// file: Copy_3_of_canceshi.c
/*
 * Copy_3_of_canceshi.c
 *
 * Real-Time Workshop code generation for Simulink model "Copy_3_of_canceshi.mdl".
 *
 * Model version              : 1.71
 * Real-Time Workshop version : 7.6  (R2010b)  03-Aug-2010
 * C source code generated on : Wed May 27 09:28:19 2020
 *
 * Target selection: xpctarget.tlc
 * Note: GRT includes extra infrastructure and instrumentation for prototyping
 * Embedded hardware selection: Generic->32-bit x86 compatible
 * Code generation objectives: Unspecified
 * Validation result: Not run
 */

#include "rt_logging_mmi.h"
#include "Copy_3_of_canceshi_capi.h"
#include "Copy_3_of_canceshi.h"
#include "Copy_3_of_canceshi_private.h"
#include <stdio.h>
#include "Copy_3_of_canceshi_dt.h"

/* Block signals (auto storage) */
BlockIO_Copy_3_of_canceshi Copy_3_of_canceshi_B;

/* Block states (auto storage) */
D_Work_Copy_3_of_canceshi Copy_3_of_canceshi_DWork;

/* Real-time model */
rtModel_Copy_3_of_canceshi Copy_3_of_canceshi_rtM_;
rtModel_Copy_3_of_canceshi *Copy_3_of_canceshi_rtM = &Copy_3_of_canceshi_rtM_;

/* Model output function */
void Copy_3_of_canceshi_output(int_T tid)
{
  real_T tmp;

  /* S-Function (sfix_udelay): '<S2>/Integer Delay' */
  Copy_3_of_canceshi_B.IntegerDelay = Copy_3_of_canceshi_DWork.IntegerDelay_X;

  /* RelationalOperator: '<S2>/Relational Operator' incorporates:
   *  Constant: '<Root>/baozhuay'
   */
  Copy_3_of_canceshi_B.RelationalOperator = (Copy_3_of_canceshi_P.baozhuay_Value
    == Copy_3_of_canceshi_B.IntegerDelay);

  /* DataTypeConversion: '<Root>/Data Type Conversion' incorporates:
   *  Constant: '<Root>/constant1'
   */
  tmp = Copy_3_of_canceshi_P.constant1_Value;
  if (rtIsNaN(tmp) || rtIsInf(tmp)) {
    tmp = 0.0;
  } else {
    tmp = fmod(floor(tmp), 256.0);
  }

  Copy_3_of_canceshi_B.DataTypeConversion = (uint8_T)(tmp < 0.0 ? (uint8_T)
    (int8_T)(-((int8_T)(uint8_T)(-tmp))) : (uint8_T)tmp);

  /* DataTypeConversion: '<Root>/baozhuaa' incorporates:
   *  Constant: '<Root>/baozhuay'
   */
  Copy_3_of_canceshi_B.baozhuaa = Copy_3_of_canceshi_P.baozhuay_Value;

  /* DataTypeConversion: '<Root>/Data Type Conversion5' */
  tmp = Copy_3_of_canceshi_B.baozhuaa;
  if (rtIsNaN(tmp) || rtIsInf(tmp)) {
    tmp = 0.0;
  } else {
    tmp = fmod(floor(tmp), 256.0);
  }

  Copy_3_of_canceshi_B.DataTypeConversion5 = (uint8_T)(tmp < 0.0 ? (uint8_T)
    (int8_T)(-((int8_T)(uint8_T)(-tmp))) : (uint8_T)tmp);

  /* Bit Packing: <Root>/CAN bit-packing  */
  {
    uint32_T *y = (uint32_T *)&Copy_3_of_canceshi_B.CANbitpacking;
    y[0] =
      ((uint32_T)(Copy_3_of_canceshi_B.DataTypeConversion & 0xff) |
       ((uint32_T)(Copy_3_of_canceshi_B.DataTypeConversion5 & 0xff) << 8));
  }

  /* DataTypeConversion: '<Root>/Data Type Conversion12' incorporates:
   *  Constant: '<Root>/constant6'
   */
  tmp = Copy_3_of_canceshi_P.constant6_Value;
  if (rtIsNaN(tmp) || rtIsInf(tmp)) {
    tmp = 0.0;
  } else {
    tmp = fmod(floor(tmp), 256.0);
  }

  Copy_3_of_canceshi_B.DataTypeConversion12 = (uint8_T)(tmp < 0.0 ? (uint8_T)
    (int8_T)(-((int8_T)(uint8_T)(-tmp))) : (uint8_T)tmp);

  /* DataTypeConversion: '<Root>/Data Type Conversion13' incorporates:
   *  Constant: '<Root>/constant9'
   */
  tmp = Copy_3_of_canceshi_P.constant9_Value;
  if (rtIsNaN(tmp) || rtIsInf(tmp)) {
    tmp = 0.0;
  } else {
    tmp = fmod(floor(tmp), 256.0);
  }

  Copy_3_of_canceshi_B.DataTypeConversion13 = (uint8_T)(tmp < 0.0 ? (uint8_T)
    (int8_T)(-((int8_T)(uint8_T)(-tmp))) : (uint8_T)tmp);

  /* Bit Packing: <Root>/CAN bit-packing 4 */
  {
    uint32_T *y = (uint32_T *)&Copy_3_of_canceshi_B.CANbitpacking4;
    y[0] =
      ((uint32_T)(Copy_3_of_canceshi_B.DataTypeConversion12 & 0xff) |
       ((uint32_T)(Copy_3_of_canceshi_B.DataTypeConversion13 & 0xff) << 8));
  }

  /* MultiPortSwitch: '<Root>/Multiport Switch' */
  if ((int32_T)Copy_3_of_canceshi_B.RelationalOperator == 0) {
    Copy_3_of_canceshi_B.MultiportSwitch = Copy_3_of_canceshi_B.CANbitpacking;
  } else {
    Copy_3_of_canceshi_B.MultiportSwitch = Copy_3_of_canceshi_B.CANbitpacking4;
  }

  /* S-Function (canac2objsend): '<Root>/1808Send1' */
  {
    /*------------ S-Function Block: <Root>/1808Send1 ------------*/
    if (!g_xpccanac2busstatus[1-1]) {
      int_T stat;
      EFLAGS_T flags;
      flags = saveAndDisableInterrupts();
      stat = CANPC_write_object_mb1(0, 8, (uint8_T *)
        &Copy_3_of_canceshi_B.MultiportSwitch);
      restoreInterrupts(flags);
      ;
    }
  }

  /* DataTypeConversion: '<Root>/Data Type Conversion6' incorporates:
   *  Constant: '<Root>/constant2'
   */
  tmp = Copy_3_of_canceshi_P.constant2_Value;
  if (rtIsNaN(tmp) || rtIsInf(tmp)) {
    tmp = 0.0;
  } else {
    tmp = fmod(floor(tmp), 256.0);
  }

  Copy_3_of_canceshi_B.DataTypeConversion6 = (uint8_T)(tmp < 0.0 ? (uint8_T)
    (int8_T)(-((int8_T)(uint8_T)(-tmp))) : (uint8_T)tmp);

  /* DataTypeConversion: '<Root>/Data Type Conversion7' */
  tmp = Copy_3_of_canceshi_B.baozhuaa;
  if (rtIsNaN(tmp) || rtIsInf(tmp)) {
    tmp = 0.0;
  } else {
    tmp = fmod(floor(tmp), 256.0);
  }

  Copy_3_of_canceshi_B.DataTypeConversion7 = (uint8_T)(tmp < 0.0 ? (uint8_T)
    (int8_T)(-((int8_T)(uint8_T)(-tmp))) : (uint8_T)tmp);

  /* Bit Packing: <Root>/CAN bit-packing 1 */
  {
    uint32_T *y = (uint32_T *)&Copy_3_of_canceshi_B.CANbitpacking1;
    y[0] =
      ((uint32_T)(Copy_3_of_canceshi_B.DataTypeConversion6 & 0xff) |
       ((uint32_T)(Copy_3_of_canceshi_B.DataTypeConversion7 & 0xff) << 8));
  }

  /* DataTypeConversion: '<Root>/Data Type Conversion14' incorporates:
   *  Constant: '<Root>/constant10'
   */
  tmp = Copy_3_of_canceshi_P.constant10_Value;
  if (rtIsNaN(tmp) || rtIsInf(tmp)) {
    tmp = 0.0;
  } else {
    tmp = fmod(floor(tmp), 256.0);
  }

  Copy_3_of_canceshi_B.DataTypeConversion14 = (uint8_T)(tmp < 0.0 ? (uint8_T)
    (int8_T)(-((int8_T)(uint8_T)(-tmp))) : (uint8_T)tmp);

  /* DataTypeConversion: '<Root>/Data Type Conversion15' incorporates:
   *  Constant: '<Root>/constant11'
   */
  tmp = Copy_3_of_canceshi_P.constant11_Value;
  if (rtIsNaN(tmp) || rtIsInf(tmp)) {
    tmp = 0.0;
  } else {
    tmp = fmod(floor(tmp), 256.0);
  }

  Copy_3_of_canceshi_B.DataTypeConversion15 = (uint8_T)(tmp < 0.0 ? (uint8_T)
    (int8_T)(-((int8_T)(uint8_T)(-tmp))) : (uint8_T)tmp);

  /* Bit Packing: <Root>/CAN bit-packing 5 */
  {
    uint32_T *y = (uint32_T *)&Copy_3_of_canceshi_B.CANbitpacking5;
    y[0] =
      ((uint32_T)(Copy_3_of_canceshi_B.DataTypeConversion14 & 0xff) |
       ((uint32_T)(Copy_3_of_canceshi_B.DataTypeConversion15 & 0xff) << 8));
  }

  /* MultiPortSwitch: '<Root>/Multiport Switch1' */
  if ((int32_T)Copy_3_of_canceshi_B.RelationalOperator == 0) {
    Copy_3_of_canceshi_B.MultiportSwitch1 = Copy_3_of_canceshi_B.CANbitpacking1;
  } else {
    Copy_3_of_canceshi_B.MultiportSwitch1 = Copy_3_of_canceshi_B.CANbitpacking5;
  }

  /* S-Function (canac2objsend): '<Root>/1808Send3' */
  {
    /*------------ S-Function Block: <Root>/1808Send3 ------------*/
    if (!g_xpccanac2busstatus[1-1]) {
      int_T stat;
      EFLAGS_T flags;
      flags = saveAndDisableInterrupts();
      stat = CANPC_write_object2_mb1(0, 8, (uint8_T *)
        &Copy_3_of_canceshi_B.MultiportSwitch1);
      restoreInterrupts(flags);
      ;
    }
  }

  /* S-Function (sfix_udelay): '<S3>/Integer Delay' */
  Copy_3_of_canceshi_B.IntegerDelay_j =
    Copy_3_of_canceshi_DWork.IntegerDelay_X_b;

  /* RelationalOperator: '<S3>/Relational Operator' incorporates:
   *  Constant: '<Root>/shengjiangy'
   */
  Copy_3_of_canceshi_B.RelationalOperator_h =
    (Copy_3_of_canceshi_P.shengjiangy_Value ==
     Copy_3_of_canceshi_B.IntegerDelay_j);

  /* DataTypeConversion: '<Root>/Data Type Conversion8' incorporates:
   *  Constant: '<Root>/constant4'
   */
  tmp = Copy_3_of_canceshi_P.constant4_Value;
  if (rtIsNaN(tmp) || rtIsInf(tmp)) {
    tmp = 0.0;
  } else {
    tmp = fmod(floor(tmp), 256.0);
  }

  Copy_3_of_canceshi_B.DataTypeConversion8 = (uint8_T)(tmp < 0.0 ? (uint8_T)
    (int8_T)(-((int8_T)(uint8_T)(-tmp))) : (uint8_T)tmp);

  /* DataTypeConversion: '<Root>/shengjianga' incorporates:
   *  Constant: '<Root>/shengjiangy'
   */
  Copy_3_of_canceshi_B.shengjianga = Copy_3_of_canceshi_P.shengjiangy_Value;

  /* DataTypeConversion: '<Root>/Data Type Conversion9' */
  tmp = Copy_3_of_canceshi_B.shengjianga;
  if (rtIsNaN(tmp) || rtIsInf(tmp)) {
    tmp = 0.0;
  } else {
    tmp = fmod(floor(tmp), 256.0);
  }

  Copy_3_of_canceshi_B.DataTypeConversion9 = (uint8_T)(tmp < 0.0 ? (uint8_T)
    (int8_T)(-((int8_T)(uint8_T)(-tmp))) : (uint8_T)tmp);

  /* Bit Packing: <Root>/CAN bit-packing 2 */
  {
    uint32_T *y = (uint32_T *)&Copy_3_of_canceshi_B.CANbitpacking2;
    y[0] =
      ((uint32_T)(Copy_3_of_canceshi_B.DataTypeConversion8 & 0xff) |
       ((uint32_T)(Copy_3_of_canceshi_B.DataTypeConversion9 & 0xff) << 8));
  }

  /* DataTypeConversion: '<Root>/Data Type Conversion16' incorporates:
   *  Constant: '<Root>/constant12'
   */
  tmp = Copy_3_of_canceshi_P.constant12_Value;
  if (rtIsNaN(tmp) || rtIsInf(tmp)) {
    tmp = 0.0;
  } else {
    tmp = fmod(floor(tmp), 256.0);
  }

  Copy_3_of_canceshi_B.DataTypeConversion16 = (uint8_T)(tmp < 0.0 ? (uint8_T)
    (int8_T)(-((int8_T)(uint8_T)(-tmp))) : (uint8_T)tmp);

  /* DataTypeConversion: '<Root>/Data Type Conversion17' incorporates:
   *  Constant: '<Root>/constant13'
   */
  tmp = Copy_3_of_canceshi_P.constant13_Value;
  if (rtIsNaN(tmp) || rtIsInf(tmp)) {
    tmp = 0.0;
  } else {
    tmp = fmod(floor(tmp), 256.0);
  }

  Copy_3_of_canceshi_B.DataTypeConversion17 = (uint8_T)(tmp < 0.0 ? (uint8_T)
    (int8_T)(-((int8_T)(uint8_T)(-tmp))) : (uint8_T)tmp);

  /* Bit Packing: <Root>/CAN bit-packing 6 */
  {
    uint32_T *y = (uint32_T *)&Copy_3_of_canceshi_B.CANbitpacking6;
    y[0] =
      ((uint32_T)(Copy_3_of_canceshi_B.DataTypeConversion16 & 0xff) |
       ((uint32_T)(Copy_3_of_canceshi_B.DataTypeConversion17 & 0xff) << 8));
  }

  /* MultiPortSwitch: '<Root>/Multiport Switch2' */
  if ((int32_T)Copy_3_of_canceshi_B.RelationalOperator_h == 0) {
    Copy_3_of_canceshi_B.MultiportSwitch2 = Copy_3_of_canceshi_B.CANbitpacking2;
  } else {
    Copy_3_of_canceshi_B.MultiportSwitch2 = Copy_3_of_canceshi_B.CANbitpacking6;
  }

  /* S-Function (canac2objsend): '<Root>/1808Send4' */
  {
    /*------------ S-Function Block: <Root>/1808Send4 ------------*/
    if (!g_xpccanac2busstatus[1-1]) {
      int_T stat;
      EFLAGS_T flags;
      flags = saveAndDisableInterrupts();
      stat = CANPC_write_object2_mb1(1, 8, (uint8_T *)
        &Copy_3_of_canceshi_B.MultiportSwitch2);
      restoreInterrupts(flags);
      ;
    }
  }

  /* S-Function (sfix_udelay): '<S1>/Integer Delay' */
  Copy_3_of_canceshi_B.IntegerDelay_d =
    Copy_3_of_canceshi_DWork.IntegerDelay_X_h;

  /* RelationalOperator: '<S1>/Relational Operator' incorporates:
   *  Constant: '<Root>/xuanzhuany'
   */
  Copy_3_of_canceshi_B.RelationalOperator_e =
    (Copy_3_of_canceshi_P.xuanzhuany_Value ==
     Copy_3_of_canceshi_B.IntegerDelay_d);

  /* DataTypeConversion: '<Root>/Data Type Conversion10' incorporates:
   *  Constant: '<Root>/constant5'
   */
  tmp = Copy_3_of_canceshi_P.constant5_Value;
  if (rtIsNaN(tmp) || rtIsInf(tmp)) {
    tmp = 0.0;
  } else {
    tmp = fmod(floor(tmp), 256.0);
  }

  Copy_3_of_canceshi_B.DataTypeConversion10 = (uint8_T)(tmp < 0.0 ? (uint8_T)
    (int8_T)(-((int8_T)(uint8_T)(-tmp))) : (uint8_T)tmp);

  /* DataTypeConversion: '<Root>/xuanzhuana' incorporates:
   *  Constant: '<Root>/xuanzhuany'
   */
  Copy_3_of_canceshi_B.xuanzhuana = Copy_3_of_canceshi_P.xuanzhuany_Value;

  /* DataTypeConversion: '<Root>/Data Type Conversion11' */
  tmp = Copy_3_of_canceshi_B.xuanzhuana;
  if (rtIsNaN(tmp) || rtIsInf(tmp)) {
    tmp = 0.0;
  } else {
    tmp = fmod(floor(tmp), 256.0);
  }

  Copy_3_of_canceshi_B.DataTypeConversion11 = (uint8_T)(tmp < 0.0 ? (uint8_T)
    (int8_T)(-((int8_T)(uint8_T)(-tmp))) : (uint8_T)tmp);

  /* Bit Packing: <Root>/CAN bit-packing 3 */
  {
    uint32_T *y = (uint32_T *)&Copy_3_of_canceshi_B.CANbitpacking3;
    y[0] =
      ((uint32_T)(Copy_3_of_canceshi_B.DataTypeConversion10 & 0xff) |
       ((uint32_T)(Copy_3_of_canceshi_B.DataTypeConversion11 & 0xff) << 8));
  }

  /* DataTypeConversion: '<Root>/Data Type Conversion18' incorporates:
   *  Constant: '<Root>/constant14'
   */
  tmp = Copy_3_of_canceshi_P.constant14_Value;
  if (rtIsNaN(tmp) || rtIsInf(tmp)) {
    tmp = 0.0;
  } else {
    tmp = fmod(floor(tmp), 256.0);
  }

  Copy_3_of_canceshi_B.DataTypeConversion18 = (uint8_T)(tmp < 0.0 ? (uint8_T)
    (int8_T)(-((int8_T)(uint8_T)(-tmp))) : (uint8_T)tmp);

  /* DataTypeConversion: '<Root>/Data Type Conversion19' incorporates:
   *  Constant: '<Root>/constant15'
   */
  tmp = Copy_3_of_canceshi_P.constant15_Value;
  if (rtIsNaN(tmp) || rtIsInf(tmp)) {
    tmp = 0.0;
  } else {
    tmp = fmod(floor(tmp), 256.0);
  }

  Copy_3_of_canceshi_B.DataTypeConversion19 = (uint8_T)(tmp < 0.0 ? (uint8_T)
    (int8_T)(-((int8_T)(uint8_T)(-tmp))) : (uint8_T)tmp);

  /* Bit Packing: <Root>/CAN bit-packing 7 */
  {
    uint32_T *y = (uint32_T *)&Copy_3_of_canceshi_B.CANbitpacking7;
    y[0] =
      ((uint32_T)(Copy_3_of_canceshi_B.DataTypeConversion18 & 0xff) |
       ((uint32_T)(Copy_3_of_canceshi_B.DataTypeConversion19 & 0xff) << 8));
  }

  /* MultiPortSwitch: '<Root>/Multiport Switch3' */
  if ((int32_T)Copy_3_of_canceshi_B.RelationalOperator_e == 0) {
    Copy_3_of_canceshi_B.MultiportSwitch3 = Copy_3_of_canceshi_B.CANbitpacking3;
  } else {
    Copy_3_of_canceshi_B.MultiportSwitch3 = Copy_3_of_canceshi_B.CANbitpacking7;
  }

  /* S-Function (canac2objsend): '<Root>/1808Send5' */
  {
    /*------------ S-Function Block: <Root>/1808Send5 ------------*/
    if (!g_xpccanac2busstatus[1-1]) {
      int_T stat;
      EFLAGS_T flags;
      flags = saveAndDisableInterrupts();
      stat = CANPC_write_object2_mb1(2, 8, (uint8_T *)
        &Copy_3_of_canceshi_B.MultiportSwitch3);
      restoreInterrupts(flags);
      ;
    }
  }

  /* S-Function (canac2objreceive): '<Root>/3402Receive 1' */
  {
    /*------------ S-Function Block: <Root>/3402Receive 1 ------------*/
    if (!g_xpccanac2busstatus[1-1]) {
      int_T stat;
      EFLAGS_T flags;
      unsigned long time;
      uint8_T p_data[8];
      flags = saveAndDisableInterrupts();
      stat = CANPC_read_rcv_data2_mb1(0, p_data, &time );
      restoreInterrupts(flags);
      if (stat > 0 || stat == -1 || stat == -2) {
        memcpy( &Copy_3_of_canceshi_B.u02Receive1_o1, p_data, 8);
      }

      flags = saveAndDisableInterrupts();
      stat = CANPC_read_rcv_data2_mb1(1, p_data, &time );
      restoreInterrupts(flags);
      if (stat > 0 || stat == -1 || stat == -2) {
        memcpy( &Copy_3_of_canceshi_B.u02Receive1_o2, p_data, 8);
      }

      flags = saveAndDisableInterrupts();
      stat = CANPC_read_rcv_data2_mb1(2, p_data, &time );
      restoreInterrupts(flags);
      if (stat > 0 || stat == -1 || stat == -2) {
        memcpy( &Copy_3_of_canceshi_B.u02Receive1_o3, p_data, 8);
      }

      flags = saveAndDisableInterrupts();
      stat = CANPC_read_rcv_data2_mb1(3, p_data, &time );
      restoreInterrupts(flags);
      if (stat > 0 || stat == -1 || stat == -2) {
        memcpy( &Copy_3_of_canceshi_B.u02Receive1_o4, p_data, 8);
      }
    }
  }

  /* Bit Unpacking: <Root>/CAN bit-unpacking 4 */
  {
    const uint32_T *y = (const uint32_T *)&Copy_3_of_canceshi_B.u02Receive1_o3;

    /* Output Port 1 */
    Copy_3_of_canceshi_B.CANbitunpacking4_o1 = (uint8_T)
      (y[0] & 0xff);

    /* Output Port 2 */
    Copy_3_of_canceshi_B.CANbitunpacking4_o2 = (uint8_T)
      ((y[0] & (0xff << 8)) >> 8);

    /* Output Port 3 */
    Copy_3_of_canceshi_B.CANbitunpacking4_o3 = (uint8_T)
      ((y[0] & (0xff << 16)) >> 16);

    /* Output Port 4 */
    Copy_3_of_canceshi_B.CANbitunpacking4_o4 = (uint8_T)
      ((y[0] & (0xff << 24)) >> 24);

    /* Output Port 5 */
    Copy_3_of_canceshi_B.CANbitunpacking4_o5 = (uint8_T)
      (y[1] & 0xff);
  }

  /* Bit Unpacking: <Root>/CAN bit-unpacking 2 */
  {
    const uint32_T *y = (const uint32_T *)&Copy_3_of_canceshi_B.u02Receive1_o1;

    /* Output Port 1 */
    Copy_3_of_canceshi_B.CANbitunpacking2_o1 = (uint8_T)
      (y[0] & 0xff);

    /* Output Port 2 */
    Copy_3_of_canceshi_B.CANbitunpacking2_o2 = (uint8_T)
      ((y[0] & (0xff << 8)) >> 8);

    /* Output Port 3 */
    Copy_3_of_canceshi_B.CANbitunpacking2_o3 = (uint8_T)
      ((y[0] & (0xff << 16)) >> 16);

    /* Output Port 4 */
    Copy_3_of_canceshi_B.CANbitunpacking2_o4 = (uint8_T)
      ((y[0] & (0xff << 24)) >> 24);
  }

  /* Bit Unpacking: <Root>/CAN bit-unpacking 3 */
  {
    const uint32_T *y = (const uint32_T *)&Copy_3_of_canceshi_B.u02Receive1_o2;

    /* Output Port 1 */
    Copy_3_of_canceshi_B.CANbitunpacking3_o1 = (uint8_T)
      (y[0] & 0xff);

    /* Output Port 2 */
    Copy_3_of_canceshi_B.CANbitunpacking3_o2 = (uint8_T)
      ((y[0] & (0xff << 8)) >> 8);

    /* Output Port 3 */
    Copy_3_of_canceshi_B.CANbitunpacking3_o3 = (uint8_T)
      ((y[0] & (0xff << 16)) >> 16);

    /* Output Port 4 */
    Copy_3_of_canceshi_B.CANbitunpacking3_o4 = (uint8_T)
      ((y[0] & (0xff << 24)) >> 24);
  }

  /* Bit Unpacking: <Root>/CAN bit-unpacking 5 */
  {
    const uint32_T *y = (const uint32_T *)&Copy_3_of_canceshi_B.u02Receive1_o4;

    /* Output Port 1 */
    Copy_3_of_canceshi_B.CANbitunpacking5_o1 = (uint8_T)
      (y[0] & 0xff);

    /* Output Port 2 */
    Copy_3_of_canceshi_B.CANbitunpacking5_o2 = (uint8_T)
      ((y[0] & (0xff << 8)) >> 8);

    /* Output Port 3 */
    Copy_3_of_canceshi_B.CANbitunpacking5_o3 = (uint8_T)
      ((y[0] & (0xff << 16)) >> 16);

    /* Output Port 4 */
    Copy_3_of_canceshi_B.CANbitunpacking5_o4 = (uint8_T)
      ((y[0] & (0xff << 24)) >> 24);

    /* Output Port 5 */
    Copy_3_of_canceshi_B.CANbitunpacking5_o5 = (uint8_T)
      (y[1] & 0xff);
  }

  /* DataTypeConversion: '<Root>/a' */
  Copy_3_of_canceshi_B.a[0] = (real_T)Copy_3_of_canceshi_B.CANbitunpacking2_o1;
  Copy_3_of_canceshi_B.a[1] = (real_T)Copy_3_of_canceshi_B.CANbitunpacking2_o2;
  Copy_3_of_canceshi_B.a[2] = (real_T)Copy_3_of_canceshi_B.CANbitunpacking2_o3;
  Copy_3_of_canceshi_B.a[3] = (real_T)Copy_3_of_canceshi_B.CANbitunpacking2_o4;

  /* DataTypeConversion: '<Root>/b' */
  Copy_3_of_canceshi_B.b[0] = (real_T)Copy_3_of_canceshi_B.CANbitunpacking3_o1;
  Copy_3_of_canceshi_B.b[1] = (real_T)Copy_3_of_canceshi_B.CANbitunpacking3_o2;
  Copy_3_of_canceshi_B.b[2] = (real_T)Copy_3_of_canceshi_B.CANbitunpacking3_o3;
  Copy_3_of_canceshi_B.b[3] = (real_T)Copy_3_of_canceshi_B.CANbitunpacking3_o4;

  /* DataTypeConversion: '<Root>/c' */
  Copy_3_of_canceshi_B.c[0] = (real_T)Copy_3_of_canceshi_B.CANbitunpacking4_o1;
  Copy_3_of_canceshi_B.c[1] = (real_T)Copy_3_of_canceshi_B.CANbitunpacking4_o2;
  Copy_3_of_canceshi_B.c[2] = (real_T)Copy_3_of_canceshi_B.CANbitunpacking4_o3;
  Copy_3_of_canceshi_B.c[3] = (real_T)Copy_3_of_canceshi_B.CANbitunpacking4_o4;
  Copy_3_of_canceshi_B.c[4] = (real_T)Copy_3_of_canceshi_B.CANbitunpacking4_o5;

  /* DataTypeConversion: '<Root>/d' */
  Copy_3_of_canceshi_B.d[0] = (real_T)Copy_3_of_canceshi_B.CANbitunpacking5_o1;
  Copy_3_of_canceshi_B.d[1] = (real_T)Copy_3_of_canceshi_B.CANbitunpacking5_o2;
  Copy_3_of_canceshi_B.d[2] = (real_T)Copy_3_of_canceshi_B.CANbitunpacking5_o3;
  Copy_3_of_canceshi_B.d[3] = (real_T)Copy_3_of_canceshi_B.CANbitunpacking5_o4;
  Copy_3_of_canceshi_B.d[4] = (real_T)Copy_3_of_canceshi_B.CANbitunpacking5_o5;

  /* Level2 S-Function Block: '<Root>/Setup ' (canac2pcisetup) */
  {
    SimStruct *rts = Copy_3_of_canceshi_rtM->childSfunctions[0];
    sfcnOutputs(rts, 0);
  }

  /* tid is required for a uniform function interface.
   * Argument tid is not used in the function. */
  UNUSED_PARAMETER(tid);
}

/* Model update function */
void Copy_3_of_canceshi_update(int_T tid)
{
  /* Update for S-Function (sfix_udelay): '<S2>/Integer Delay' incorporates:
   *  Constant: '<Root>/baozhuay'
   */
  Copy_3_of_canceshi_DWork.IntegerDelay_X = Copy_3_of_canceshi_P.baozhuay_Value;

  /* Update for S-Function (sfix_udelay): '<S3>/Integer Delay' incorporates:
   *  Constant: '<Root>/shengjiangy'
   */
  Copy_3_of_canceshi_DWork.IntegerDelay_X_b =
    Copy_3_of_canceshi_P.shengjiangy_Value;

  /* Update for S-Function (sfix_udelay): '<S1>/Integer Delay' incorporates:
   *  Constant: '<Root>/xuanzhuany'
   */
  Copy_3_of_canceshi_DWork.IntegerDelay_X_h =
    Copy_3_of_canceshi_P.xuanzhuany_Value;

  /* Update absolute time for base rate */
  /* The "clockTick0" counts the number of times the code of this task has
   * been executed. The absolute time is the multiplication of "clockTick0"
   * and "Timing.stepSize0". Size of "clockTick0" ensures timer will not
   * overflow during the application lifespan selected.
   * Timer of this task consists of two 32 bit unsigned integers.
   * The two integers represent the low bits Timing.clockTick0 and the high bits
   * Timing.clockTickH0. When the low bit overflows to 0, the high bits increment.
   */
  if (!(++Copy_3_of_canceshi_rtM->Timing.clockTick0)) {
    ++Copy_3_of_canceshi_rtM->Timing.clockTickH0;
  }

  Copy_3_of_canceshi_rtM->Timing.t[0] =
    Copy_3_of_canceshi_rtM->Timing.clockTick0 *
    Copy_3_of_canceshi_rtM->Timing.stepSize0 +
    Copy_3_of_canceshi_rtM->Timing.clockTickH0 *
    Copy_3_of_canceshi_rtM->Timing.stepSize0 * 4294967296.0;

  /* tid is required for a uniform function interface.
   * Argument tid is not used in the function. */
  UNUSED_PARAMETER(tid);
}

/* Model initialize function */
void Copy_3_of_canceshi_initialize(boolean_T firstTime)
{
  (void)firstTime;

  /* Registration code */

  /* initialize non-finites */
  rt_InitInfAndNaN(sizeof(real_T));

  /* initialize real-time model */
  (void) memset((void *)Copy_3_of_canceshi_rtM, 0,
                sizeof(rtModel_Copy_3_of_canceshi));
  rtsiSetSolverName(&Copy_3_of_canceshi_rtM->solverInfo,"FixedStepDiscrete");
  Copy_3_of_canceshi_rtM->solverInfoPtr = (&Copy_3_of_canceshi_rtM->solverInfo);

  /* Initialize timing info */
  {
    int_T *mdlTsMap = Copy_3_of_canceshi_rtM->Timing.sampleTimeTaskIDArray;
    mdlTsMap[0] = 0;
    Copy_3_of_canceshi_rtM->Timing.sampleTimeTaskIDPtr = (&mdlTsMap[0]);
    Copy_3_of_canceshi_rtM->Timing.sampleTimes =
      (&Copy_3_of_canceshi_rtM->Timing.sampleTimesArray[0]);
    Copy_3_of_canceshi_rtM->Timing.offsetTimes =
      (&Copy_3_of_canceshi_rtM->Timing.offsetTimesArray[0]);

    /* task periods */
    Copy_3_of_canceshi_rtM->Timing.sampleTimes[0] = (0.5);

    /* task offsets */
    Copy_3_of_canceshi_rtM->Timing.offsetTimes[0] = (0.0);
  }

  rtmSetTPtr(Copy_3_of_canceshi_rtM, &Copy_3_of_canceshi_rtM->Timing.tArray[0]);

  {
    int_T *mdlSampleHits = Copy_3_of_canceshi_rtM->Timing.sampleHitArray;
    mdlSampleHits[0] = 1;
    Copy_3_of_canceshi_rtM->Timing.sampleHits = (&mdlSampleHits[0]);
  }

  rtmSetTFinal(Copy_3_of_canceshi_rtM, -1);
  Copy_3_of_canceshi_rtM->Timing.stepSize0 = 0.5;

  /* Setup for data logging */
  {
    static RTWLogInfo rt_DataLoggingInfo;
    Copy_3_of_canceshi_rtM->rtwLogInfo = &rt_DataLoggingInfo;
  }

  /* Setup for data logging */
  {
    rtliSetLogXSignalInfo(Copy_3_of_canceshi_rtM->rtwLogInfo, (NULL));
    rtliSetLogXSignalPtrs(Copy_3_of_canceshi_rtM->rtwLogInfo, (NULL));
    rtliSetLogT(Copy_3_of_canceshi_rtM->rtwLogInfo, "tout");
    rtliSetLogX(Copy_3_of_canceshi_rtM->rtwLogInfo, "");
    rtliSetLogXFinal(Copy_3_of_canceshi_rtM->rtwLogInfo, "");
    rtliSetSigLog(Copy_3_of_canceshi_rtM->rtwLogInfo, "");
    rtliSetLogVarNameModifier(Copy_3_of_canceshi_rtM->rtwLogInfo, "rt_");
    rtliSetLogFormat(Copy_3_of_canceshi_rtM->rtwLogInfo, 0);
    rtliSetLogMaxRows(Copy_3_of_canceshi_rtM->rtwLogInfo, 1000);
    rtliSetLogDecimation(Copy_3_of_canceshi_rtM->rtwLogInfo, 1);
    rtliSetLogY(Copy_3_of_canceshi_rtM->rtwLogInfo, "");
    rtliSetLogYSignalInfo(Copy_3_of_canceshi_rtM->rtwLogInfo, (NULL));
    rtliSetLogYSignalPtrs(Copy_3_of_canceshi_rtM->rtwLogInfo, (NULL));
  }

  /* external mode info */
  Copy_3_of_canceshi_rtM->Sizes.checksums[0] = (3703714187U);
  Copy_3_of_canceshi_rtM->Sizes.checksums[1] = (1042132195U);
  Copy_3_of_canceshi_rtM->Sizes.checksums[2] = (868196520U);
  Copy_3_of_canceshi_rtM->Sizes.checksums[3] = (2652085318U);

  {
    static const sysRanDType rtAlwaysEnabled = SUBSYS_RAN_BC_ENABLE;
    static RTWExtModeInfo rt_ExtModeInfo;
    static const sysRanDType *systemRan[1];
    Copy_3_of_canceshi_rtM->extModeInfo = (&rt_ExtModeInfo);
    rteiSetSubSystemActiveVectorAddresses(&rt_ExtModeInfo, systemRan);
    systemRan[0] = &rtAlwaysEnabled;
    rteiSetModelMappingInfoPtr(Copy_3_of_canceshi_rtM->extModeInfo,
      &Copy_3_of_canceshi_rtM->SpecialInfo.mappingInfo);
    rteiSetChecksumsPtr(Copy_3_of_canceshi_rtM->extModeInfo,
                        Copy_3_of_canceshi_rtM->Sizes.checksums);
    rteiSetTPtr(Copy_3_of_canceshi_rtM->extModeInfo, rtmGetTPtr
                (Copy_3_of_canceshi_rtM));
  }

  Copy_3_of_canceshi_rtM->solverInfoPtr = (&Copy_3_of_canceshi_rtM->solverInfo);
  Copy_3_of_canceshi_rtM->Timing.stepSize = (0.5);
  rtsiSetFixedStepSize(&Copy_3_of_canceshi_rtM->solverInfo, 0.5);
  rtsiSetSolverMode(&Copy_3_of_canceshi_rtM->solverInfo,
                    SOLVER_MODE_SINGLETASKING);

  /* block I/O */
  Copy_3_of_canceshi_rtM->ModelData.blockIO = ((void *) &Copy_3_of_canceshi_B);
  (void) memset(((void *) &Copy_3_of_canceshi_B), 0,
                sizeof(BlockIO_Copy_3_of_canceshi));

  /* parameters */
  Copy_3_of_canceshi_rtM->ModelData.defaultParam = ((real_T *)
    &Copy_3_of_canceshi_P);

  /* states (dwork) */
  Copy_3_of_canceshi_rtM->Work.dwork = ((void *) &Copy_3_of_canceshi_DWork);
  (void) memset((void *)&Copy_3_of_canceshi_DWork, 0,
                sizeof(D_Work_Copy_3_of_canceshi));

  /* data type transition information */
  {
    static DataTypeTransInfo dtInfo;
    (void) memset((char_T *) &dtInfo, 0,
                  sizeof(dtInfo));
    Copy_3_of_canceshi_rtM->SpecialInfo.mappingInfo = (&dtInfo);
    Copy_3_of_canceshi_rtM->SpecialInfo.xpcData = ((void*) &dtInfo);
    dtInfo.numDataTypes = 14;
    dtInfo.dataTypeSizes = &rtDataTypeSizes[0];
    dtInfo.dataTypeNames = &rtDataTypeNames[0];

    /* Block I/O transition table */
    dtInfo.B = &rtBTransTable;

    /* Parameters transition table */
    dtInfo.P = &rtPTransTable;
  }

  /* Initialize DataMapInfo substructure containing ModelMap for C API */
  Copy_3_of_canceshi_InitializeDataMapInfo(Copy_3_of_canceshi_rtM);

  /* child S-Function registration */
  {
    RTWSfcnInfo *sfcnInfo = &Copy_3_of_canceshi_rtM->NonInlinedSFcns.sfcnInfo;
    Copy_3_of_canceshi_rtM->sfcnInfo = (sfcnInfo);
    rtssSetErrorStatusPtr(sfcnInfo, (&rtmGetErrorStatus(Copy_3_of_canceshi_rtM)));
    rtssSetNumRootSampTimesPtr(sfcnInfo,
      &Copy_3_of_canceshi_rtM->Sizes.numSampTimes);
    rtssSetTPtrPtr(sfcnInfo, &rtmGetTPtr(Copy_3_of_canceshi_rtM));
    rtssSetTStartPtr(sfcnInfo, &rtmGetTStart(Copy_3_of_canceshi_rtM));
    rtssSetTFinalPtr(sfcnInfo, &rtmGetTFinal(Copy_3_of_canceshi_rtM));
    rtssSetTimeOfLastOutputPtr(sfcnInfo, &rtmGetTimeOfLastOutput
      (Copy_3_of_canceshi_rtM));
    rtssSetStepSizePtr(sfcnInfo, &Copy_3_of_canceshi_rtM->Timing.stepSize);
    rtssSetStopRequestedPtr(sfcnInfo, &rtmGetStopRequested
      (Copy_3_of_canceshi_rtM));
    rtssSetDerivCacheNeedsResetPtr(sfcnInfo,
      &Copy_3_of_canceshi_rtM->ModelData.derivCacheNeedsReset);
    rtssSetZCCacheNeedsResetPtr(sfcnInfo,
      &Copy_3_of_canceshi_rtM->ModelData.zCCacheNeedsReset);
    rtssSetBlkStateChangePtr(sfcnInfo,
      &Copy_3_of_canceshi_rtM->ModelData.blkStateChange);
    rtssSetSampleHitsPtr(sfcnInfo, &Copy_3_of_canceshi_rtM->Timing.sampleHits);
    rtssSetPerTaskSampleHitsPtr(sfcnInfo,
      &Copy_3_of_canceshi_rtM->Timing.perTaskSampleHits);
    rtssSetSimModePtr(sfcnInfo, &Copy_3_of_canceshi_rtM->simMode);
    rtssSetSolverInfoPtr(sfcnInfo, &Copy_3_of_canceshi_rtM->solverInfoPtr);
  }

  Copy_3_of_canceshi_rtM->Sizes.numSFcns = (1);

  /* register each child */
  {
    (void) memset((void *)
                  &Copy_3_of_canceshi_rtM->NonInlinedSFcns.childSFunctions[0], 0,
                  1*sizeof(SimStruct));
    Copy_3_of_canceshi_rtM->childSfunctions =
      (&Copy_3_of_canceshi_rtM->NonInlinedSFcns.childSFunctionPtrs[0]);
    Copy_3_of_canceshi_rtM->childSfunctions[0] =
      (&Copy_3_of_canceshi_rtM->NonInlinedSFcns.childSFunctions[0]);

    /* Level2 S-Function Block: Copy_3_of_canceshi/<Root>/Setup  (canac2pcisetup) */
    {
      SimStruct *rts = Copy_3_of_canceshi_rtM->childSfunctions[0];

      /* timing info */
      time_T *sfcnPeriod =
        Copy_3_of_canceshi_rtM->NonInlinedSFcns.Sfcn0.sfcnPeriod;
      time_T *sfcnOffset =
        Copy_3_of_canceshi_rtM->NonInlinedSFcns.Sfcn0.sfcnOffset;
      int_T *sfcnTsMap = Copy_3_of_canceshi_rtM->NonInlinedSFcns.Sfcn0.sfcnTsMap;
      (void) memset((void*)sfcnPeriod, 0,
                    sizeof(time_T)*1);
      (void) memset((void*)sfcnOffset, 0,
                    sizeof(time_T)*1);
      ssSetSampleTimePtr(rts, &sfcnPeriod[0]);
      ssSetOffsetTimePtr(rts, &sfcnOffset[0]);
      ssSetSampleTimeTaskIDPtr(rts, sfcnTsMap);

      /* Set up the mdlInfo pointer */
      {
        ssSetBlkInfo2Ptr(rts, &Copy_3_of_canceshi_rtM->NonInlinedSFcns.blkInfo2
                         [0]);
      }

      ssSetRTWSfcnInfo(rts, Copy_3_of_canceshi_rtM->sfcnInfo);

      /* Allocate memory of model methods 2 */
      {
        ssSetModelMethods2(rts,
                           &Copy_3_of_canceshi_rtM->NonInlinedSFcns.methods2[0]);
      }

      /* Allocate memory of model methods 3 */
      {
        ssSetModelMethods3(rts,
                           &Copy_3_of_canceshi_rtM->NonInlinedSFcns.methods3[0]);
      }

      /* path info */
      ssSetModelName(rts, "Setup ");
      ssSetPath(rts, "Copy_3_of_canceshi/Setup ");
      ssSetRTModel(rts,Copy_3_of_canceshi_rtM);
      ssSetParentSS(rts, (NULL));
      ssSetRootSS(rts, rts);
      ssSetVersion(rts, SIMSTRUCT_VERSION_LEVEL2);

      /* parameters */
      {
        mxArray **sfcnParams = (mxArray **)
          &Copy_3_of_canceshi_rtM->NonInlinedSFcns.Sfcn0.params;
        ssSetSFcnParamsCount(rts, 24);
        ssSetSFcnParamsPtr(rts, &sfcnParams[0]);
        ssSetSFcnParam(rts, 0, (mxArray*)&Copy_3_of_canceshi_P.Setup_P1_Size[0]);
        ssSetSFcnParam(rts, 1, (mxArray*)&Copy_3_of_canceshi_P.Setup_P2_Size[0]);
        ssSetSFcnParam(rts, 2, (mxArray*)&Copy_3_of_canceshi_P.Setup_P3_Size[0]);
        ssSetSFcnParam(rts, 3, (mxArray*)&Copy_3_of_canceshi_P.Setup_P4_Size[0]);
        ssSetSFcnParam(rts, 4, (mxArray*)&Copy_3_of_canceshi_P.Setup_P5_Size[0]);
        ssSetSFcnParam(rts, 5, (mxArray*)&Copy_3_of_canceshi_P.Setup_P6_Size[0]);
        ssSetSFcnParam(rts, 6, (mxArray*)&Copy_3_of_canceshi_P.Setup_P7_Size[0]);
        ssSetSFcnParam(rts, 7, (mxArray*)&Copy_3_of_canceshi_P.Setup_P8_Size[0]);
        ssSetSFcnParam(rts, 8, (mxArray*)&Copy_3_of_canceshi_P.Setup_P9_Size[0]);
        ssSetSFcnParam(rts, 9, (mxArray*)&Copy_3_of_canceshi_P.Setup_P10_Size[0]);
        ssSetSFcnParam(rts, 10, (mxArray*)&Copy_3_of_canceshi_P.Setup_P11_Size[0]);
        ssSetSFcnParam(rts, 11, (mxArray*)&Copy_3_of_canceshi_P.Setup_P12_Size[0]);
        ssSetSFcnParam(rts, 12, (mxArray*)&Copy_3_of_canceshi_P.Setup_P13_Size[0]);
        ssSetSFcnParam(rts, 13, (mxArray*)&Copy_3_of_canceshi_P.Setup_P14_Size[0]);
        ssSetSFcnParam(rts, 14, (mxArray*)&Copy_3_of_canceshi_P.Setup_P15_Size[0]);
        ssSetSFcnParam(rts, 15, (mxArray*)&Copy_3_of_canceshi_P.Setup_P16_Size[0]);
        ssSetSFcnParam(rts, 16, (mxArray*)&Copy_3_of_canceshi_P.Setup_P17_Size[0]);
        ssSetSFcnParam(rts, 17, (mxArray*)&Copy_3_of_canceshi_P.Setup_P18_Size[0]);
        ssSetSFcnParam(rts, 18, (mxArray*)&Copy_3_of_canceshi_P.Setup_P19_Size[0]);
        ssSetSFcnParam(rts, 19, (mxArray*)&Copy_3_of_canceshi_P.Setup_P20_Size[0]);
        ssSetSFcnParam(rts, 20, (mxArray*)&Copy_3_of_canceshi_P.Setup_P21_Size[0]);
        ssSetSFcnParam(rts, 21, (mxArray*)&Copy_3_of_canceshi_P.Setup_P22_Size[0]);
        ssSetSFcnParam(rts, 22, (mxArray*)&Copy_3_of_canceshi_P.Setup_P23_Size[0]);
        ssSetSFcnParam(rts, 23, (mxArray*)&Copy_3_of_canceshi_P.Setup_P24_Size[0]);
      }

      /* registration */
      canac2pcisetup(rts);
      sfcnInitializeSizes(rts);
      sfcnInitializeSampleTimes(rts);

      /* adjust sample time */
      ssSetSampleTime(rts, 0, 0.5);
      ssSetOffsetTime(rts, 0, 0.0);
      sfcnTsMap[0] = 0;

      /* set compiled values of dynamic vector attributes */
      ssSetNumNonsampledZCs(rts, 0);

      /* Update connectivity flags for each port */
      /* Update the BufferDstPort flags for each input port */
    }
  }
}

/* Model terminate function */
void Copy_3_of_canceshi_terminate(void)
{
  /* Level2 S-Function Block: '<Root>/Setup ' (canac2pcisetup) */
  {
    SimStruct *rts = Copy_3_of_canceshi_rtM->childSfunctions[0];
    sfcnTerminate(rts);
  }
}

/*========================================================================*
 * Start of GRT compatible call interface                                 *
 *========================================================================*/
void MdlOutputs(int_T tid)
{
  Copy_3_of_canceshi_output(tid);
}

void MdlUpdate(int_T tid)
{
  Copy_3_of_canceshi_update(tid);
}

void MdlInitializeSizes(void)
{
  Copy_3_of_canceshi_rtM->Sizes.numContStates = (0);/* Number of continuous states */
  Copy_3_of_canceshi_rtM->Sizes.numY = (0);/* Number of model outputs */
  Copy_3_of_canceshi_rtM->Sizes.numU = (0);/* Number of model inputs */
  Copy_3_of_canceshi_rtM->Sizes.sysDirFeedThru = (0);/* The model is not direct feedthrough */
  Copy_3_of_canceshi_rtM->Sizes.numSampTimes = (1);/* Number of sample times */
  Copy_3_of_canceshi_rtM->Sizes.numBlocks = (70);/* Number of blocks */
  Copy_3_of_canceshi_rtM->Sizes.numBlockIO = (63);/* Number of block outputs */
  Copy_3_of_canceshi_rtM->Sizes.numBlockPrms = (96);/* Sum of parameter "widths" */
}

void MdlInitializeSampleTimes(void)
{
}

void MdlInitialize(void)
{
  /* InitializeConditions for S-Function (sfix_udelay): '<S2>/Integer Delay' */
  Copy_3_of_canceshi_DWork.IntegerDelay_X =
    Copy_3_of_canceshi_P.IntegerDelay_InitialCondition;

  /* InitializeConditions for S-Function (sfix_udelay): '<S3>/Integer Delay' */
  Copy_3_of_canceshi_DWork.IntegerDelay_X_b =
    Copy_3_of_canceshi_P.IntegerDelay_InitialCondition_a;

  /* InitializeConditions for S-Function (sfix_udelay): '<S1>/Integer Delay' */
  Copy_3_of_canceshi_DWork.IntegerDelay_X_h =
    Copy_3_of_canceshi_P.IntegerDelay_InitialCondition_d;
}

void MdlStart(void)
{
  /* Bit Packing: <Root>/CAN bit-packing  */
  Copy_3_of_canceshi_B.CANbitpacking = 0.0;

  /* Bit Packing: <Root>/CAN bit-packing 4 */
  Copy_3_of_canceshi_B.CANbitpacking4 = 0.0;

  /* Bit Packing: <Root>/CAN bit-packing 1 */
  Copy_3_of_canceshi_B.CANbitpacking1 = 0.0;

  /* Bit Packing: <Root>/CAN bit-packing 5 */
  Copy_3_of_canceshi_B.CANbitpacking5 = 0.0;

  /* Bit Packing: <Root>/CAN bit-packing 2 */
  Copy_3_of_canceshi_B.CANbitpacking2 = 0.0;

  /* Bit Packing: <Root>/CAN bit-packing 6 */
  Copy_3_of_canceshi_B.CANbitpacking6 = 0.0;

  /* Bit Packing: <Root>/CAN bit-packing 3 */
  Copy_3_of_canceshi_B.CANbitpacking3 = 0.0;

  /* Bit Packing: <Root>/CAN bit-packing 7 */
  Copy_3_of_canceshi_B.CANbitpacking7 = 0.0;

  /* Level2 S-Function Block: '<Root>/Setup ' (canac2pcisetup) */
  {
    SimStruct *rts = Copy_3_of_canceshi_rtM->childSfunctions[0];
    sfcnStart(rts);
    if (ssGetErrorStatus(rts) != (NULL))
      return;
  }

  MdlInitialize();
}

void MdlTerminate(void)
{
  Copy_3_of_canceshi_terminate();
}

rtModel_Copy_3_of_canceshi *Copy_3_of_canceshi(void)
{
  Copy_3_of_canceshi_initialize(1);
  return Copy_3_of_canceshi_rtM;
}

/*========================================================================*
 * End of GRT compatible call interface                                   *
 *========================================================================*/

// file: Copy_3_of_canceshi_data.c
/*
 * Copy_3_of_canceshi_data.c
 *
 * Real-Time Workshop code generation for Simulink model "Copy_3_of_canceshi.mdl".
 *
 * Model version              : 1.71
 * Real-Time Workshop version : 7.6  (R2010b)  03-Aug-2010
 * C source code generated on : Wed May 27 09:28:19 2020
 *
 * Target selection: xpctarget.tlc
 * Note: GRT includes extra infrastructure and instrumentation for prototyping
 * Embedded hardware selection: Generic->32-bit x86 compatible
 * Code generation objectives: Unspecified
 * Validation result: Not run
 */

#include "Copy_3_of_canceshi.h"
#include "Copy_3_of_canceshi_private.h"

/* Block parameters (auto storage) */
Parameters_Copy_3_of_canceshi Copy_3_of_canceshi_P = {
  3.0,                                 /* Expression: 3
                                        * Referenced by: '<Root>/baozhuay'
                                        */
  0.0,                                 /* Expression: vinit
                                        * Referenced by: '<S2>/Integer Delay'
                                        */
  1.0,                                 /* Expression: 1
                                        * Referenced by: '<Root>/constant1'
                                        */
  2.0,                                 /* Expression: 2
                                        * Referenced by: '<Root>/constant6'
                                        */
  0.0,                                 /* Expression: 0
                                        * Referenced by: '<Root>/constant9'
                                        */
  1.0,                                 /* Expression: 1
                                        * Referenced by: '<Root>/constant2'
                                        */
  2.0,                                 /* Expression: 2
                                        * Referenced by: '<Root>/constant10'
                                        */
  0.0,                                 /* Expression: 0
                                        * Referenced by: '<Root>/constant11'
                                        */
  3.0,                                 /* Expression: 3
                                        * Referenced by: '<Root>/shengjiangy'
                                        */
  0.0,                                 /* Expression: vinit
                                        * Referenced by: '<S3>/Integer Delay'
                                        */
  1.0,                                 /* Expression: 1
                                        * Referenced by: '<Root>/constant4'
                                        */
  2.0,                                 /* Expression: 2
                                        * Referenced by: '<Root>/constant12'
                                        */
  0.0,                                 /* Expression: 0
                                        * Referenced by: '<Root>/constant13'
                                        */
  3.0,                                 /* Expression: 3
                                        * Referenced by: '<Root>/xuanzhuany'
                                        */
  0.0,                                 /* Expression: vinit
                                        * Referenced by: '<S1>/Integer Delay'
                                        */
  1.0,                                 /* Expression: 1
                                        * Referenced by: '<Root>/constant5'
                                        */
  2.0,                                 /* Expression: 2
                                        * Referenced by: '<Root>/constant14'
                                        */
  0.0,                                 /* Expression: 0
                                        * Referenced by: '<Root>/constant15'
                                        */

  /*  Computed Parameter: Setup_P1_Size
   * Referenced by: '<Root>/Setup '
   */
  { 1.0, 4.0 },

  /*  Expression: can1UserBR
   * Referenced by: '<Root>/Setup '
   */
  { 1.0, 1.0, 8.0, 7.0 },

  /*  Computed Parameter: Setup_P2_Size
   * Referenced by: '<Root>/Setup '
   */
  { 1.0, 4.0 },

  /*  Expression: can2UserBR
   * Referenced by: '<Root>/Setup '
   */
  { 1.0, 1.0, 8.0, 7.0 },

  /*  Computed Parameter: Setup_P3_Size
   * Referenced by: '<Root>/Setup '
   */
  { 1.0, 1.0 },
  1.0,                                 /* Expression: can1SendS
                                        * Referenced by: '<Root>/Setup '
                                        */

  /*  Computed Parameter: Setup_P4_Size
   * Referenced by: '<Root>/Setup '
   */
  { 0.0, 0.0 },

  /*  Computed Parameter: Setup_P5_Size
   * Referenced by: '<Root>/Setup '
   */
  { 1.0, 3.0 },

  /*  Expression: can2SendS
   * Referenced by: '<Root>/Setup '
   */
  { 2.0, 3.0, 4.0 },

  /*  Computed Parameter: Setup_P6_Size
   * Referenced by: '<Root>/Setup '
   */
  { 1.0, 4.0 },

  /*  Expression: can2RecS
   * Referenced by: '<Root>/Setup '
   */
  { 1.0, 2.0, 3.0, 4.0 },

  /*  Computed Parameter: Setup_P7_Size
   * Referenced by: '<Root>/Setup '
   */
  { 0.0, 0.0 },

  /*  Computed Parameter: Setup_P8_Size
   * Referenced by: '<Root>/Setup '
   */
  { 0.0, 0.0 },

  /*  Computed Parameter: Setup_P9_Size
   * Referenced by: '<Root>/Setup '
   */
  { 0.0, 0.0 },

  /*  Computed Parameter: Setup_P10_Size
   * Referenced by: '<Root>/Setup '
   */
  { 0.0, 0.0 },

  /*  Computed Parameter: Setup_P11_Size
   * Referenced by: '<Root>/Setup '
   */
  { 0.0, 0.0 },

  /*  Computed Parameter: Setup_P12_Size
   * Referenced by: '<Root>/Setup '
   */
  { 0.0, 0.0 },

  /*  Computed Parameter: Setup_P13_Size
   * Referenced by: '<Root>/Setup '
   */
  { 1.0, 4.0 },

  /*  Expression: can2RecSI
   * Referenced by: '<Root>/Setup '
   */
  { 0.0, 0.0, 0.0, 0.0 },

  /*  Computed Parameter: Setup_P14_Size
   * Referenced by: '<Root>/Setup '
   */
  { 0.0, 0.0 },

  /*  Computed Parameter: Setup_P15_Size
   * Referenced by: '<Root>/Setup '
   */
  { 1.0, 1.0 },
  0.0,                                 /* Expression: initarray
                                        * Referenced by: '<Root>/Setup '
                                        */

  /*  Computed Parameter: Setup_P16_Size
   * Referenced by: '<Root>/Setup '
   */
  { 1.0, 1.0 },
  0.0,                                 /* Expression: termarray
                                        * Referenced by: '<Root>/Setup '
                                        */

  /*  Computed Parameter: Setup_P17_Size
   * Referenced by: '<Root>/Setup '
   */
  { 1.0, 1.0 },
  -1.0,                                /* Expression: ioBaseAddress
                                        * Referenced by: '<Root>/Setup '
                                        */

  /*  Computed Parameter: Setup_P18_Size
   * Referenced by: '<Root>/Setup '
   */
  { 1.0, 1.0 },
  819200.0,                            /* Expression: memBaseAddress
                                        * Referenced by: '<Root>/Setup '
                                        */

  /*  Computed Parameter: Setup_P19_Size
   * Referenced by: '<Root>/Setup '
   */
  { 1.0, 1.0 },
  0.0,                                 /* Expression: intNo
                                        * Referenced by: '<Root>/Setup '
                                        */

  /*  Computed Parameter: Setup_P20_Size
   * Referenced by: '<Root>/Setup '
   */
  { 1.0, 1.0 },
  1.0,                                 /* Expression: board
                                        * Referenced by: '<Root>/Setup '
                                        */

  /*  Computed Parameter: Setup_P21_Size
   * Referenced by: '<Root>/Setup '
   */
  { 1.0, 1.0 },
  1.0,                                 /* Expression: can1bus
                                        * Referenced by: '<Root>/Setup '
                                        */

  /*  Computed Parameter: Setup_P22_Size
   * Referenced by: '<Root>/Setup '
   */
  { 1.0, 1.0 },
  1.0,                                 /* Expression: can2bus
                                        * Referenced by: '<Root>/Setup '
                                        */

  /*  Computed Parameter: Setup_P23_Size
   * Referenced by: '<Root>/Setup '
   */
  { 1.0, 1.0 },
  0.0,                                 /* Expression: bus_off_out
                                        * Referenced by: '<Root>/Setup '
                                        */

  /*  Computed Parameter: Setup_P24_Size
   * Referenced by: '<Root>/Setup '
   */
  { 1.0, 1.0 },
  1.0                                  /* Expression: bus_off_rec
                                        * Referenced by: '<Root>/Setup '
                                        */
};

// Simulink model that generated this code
simulink model "Copy_3_of_canceshi"  (Simulink 7.6)
settings: Solver=ode4  StartTime=0.0  StopTime=inf  FixedStep=0.5  RelTol=1e-3
undefined symbols (not defined in the file or in its folder): bit, Standard
libraries: xpclib x18, simulink x3

== system Copy_3_of_canceshi ==
  1808Send1 : xpclib/CAN/Softing/CAN-AC2-PCI SJA 1000/Send   board=1  canPort=CAN 1  range=Standard (11-bit)  ids=1  sizes=[8]  output=off  ts=-1  ididx=[0]
  1808Send3 : xpclib/CAN/Softing/CAN-AC2-PCI SJA 1000/Send   board=1  canPort=CAN 2  range=Standard (11-bit)  ids=2  sizes=[8]  output=off  ts=-1  ididx=[1]
  1808Send4 : xpclib/CAN/Softing/CAN-AC2-PCI SJA 1000/Send   board=1  canPort=CAN 2  range=Standard (11-bit)  ids=3  sizes=[8]  output=off  ts=-1  ididx=[2]
  1808Send5 : xpclib/CAN/Softing/CAN-AC2-PCI SJA 1000/Send   board=1  canPort=CAN 2  range=Standard (11-bit)  ids=4  sizes=[8]  output=off  ts=-1  ididx=[3]
  3402Receive 1 : xpclib/CAN/Softing/CAN-AC2-PCI SJA 1000/Receive   board=1  canPort=CAN 2  range=Standard (11-bit)  ids=[1 2 3 4]  lengths=8  output=Data  inten=off  ts=-1  ididx=[0,1,2,3]
  CAN bit-packing {,1..7} (8 alike) : xpclib/CAN/Utilities/CAN bit-packing   bitpatterns={ [0:7] [8:15] }
  CAN bit-unpacking 2 : xpclib/CAN/Utilities/CAN bit-unpacking   bitpatterns={ [0:7],[8:15],[16:23],[24:31]}  dtypes={ 'uint8','uint8','uint8','uint8' }
  CAN bit-unpacking 3 : xpclib/CAN/Utilities/CAN bit-unpacking   bitpatterns={ [0:7],[8:15],[16:23],[24:31]}  dtypes={ 'uint8','uint8','uint8','uint8' }
  CAN bit-unpacking 4 : xpclib/CAN/Utilities/CAN bit-unpacking   bitpatterns={ [0:7],[8:15],[16:23],[24:31],[32:39]}  dtypes={ 'uint8','uint8','uint8','uint8','uint8' }
  CAN bit-unpacking 5 : xpclib/CAN/Utilities/CAN bit-unpacking   bitpatterns={ [0:7],[8:15],[16:23],[24:31],[32:39]}  dtypes={ 'uint8','uint8','uint8','uint8','uint8' }
  Data Type Conversion{,5..19} (16 alike) : DataTypeConversion  OutDataTypeStr=uint8
  Multiport Switch{,1..3} (4 alike) : MultiPortSwitch  DataPortOrder=Zero-based contiguous  Inputs=2  zeroidx=on
  Mux3 : Mux
  Mux4 : Mux
  Mux5 : Mux  Inputs=5
  Mux6 : Mux  Inputs=5
  "Setup " : xpclib/CAN/Softing/CAN-AC2-PCI SJA 1000/Setup   board=1  can1bus=Highspeed (ISO 11898)  can1Baudrate=500 kBaud  can1UserBR=[1,1,4,3]  can2bus=Highspeed (ISO 11898)  can2Baudrate=500 kBaud  can2UserBR=[1,1,4,3]  init=[]  term=[]  bus_off_out=off  bus_off_rec=Off  ioBaseAddress=-1
  Subsystem1 : Subsystem
  Subsystem2 : Subsystem
  Subsystem3 : Subsystem
  Terminator{1..4} (4 alike) : Terminator
  a : DataTypeConversion  OutDataTypeStr=double
  b : DataTypeConversion  OutDataTypeStr=double
  baozhuaa : DataTypeConversion
  baozhuay : Constant  Value=3
  c : DataTypeConversion  OutDataTypeStr=double
  chuanganqi{1..4} (4 alike) : Display
  constant{1..2,4..5} (4 alike) : Constant
  constant{6,10,12,14} (4 alike) : Constant  Value=2
  constant{9,11,13,15} (4 alike) : Constant  Value=0
  d : DataTypeConversion  OutDataTypeStr=double
  shengjianga : DataTypeConversion
  shengjiangy : Constant  Value=3
  xuanzhuana : DataTypeConversion
  xuanzhuany : Constant  Value=3
  wires:
  3402Receive 1/1 -> CAN bit-unpacking 2/1
  3402Receive 1/2 -> CAN bit-unpacking 3/1
  3402Receive 1/3 -> CAN bit-unpacking 4/1
  3402Receive 1/4 -> CAN bit-unpacking 5/1
  CAN bit-unpacking 2/1 -> Mux3/1
  CAN bit-unpacking 2/2 -> Mux3/2
  CAN bit-unpacking 2/3 -> Mux3/3
  CAN bit-unpacking 2/4 -> Mux3/4
  CAN bit-unpacking 3/1 -> Mux4/1
  CAN bit-unpacking 3/2 -> Mux4/2
  CAN bit-unpacking 3/3 -> Mux4/3
  CAN bit-unpacking 3/4 -> Mux4/4
  CAN bit-unpacking 4/1 -> Mux5/1
  CAN bit-unpacking 4/2 -> Mux5/2
  CAN bit-unpacking 4/3 -> Mux5/3
  CAN bit-unpacking 4/4 -> Mux5/4
  CAN bit-unpacking 4/5 -> Mux5/5
  CAN bit-unpacking 5/1 -> Mux6/1
  CAN bit-unpacking 5/2 -> Mux6/2
  CAN bit-unpacking 5/3 -> Mux6/3
  CAN bit-unpacking 5/4 -> Mux6/4
  CAN bit-unpacking 5/5 -> Mux6/5
  Mux3/1 -> chuanganqi2/1, a/1
  Mux4/1 -> b/1, chuanganqi3/1
  Mux5/1 -> c/1, chuanganqi1/1
  Mux6/1 -> d/1, chuanganqi4/1
  b/1 -> Terminator1/1
  c/1 -> Terminator2/1
  d/1 -> Terminator3/1
  a/1 -> Terminator4/1
  constant1/1 -> Data Type Conversion/1
  Data Type Conversion/1 -> "CAN bit-packing "/1
  Data Type Conversion5/1 -> "CAN bit-packing "/2
  constant2/1 -> Data Type Conversion6/1
  Data Type Conversion6/1 -> CAN bit-packing 1/1
  Data Type Conversion7/1 -> CAN bit-packing 1/2
  constant4/1 -> Data Type Conversion8/1
  Data Type Conversion8/1 -> CAN bit-packing 2/1
  Data Type Conversion9/1 -> CAN bit-packing 2/2
  constant5/1 -> Data Type Conversion10/1
  Data Type Conversion10/1 -> CAN bit-packing 3/1
  Data Type Conversion11/1 -> CAN bit-packing 3/2
  constant6/1 -> Data Type Conversion12/1
  Data Type Conversion12/1 -> CAN bit-packing 4/1
  Data Type Conversion13/1 -> CAN bit-packing 4/2
  constant9/1 -> Data Type Conversion13/1
  constant10/1 -> Data Type Conversion14/1
  Data Type Conversion14/1 -> CAN bit-packing 5/1
  Data Type Conversion15/1 -> CAN bit-packing 5/2
  constant11/1 -> Data Type Conversion15/1
  constant12/1 -> Data Type Conversion16/1
  Data Type Conversion16/1 -> CAN bit-packing 6/1
  Data Type Conversion17/1 -> CAN bit-packing 6/2
  constant13/1 -> Data Type Conversion17/1
  constant14/1 -> Data Type Conversion18/1
  Data Type Conversion18/1 -> CAN bit-packing 7/1
  Data Type Conversion19/1 -> CAN bit-packing 7/2
  constant15/1 -> Data Type Conversion19/1
  Multiport Switch1/1 -> 1808Send3/1
  baozhuay/1 -> baozhuaa/1, Subsystem2/1(In1)
  shengjiangy/1 -> shengjianga/1, Subsystem3/1(In1)
  shengjianga/1 -> Data Type Conversion9/1
  xuanzhuany/1 -> xuanzhuana/1, Subsystem1/1(In1)
  xuanzhuana/1 -> Data Type Conversion11/1
  Multiport Switch3/1 -> 1808Send5/1
  Multiport Switch/1 -> 1808Send1/1
  Multiport Switch2/1 -> 1808Send4/1
  "CAN bit-packing "/1 -> Multiport Switch/2
  CAN bit-packing 4/1 -> Multiport Switch/3
  CAN bit-packing 1/1 -> Multiport Switch1/2
  CAN bit-packing 5/1 -> Multiport Switch1/3
  CAN bit-packing 2/1 -> Multiport Switch2/2
  CAN bit-packing 6/1 -> Multiport Switch2/3
  CAN bit-packing 3/1 -> Multiport Switch3/2
  CAN bit-packing 7/1 -> Multiport Switch3/3
  baozhuaa/1 -> Data Type Conversion5/1, Data Type Conversion7/1
  Subsystem2/1(Out1) -> Multiport Switch/1, Multiport Switch1/1
  Subsystem3/1(Out1) -> Multiport Switch2/1
  Subsystem1/1(Out1) -> Multiport Switch3/1

== system Copy_3_of_canceshi/Subsystem1 ==
  In1 : Inport
  Integer Delay : simulink/Discrete/Integer Delay  NumDelays=1  vinit=0.0  samptime=-1
  Relational Operator : RelationalOperator  Operator===  OutDataTypeStr=boolean
  Out1 : Outport
  wires:
  Integer Delay/1 -> Relational Operator/2
  In1/1 -> Integer Delay/1, Relational Operator/1
  Relational Operator/1 -> Out1/1

== system Copy_3_of_canceshi/Subsystem2 ==
  In1 : Inport
  Integer Delay : simulink/Discrete/Integer Delay  NumDelays=1  vinit=0.0  samptime=-1
  Relational Operator : RelationalOperator  Operator===  OutDataTypeStr=boolean
  Out1 : Outport
  wires:
  Integer Delay/1 -> Relational Operator/2
  In1/1 -> Integer Delay/1, Relational Operator/1
  Relational Operator/1 -> Out1/1

== system Copy_3_of_canceshi/Subsystem3 ==
  In1 : Inport
  Integer Delay : simulink/Discrete/Integer Delay  NumDelays=1  vinit=0.0  samptime=-1
  Relational Operator : RelationalOperator  Operator===  OutDataTypeStr=boolean
  Out1 : Outport
  wires:
  Relational Operator/1 -> Out1/1
  In1/1 -> Relational Operator/1, Integer Delay/1
  Integer Delay/1 -> Relational Operator/2
